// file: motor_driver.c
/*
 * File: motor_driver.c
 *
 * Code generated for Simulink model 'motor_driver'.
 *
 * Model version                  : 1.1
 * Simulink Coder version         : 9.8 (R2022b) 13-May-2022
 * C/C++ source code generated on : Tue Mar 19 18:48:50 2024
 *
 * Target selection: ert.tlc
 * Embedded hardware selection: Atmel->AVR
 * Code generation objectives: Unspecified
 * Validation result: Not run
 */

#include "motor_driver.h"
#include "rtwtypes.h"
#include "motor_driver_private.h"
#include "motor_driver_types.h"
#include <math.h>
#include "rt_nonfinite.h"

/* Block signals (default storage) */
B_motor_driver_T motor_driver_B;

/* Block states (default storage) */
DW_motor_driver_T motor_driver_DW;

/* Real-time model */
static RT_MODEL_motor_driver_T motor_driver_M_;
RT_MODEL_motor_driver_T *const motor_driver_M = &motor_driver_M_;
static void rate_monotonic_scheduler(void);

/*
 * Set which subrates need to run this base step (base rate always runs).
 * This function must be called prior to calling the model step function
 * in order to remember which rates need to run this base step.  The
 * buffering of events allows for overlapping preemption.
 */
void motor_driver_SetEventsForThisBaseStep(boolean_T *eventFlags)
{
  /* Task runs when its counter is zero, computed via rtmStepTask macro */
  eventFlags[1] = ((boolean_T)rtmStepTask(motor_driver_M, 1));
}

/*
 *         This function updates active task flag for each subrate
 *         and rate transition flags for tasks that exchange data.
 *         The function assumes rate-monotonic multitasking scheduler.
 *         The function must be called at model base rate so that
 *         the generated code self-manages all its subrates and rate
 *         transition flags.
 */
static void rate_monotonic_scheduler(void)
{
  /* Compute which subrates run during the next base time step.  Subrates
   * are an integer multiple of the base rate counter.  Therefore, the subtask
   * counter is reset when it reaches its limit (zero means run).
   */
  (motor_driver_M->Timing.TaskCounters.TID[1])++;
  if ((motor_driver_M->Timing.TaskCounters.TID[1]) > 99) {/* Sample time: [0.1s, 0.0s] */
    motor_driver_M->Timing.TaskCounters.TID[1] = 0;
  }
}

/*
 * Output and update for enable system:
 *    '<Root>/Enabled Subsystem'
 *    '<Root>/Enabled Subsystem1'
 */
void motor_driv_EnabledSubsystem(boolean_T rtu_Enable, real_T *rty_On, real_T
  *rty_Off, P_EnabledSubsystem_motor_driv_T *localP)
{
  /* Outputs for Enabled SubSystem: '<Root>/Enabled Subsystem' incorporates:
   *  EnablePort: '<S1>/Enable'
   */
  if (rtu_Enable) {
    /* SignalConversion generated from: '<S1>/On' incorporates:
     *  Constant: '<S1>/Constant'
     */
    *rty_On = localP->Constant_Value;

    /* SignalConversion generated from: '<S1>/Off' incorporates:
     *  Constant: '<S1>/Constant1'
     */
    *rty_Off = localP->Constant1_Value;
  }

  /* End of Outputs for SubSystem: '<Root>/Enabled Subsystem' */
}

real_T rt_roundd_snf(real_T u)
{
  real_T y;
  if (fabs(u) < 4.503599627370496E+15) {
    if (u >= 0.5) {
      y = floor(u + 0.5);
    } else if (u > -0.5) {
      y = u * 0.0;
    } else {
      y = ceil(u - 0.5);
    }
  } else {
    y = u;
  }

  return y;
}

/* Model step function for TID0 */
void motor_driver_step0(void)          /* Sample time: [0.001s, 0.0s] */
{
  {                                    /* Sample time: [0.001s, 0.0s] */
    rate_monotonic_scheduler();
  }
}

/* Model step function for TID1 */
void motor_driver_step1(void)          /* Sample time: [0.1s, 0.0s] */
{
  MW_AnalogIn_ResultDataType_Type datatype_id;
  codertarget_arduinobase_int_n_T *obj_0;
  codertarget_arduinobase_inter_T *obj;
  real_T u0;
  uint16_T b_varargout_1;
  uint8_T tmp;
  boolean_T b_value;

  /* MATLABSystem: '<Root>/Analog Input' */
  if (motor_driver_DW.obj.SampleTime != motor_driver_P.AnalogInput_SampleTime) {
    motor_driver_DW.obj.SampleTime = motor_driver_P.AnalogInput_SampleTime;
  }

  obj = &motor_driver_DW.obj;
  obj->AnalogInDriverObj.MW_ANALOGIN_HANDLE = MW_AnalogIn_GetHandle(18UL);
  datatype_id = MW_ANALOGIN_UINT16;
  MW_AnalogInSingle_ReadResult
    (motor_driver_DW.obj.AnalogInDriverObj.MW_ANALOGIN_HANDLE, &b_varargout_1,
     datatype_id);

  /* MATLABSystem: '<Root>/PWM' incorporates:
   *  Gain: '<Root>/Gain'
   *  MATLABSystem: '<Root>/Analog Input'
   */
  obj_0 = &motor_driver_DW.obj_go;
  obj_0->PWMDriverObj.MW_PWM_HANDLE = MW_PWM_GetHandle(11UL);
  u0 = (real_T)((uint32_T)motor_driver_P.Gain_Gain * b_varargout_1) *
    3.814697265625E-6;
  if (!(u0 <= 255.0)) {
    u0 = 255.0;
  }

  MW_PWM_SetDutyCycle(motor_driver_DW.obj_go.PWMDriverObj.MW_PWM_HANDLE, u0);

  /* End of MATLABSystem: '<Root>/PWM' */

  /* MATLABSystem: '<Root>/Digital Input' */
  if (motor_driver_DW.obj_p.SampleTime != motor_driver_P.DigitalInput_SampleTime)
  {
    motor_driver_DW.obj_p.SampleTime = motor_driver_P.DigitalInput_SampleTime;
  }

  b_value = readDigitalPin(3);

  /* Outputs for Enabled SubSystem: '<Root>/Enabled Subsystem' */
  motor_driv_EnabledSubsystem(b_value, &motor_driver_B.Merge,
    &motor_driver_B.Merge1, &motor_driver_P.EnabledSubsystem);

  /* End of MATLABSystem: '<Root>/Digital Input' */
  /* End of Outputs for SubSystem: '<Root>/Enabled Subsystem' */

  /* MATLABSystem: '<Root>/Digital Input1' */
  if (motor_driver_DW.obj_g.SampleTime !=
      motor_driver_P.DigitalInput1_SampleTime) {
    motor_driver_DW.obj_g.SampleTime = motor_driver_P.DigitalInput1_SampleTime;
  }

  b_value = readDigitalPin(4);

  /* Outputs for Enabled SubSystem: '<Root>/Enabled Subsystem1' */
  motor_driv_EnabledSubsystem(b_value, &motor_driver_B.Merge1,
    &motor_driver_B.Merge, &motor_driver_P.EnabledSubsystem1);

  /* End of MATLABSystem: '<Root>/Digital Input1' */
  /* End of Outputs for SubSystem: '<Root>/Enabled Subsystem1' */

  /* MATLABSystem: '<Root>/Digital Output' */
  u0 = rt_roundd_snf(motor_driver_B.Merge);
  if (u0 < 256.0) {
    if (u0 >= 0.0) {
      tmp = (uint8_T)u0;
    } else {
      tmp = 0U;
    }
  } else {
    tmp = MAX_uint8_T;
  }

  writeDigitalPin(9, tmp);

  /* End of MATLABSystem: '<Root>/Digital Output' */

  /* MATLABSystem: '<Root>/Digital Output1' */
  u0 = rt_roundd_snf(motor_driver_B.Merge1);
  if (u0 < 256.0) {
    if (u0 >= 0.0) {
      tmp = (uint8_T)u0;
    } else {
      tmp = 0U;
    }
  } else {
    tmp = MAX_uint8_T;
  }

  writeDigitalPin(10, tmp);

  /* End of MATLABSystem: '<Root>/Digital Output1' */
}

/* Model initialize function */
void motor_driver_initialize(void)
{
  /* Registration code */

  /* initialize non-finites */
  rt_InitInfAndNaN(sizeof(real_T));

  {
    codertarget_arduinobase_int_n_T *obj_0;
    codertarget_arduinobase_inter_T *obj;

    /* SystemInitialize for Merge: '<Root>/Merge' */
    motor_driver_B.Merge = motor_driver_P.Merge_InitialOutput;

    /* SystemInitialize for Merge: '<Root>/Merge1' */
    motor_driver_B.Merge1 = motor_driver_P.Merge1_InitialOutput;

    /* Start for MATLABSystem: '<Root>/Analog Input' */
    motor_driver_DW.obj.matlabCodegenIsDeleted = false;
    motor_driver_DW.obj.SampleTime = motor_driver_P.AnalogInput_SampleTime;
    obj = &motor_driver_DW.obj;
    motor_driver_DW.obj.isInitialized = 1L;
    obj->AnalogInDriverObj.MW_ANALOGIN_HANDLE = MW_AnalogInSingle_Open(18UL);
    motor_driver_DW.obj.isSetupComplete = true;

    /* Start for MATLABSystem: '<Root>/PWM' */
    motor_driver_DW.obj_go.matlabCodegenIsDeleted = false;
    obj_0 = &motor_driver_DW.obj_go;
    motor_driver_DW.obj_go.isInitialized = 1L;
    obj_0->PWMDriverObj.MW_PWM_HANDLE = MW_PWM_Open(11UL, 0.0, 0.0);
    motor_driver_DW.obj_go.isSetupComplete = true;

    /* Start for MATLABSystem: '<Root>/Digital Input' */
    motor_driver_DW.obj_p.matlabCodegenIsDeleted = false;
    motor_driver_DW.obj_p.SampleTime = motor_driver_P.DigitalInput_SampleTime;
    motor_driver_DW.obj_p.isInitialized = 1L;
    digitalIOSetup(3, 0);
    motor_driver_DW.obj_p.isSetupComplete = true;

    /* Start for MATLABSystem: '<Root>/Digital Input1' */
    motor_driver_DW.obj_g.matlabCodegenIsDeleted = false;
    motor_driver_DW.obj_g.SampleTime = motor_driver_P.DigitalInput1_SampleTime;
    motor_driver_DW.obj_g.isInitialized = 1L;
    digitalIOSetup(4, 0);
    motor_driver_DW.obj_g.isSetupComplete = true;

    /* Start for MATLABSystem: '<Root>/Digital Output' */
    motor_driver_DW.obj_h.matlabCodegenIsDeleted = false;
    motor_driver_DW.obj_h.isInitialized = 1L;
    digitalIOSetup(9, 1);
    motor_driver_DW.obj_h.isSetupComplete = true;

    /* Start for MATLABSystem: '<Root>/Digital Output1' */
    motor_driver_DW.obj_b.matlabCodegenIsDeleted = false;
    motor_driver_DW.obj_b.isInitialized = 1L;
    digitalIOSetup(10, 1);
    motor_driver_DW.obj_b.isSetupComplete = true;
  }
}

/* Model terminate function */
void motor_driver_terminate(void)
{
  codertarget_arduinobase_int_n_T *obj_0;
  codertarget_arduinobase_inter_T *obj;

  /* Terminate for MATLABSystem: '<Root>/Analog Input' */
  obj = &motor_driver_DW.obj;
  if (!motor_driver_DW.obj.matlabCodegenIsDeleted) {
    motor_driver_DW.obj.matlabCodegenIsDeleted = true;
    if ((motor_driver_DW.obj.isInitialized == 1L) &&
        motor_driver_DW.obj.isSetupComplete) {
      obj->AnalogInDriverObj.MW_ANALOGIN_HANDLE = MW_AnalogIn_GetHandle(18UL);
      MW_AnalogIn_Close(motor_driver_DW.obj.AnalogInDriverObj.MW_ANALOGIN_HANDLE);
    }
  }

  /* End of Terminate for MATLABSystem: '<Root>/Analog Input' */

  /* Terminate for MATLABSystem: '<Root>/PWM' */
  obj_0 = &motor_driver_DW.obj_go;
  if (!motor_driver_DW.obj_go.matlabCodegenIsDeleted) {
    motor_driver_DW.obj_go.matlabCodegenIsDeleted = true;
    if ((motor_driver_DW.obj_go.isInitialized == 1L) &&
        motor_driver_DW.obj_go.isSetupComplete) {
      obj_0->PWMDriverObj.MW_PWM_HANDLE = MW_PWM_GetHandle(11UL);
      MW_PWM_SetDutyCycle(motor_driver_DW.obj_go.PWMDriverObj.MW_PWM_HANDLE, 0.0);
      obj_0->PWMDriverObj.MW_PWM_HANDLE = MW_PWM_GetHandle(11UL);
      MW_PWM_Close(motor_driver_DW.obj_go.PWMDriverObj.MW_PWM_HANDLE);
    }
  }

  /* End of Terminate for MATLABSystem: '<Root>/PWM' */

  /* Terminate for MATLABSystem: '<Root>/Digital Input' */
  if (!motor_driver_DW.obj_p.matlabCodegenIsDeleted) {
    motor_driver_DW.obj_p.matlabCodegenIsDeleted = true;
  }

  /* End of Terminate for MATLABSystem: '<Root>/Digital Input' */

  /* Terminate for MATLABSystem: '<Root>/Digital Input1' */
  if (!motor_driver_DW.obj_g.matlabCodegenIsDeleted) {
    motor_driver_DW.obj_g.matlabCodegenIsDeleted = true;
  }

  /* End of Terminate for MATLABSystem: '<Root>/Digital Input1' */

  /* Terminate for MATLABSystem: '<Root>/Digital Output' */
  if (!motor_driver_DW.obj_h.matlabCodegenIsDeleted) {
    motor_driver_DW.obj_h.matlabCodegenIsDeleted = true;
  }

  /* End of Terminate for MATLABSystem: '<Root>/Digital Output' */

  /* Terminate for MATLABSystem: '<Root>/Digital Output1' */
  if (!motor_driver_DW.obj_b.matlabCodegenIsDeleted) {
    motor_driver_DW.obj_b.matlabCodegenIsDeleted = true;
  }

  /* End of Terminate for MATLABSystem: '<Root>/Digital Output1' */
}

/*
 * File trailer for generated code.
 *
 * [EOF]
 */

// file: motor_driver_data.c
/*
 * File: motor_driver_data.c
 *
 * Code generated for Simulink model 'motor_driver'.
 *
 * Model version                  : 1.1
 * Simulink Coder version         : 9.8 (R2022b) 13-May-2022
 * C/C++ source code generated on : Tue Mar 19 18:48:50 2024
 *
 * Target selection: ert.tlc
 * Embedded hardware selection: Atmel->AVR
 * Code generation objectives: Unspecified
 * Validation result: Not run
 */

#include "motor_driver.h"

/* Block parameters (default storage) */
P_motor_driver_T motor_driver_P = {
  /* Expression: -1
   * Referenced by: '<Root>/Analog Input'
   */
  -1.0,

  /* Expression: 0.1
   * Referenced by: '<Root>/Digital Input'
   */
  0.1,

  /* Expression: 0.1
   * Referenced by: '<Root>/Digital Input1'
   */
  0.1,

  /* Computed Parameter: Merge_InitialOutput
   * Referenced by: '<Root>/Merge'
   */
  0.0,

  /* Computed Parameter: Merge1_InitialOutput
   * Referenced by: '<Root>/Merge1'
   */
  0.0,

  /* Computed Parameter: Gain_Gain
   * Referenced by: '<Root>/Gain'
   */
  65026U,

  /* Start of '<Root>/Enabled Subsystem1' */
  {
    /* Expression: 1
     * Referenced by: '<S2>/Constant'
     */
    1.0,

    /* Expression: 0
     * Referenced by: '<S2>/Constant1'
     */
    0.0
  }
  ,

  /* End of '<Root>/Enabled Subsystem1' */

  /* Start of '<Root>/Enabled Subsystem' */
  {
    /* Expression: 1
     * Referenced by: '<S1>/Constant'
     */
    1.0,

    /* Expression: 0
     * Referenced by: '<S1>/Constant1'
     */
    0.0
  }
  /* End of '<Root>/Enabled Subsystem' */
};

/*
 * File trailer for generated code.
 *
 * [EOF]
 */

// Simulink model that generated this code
simulink model "motor_driver"  (R2022b)
settings: Solver=FixedStepDiscrete  StartTime=0.0  StopTime=10.0  FixedStep=1e-3  RelTol=1e-3  EnableMultiTasking=on
libraries: arduinolib x6

== system motor_driver ==
  Analog Input : arduinolib/Analog Input  pinNumber=4  ReadResultsOnly=off  ConversionTriggerSource=Software  ExternalTriggerType=uint32( 0 )  OutputDataType=uint16  EnableConversionCompleteNotify=off  EnableOuputStatus=off  SampleTime=-1  blockPlatform=arduino
  Digital Input : arduinolib/Digital Input  pinNumber=3  mode=Default  Direction=input  SampleTime=0.1  blockPlatform=arduino
  Digital Input1 : arduinolib/Digital Input  pinNumber=4  mode=Default  Direction=input  SampleTime=0.1  blockPlatform=arduino
  Digital Output : arduinolib/Digital Output  pinNumber=9  Direction=output  blockPlatform=arduino
  Digital Output1 : arduinolib/Digital Output  pinNumber=10  Direction=output  blockPlatform=arduino
  Display : Display
  Enabled Subsystem : Subsystem  TreatAsAtomicUnit=on
  Enabled Subsystem1 : Subsystem  TreatAsAtomicUnit=on
  Gain : Gain  Gain=255/1028
  Merge : Merge
  Merge1 : Merge
  PWM : arduinolib/PWM  pinNumber=11  frequencyType=Default  desiredFrequency=490.2  achievableFrequency=490.2
  wires:
  Digital Input1/1 -> Enabled Subsystem1/Enable
  Digital Input/1 -> Enabled Subsystem/Enable
  Enabled Subsystem/1(On) -> Merge/1
  Enabled Subsystem/2(Off) -> Merge1/2
  Enabled Subsystem1/1(On) -> Merge1/1
  Enabled Subsystem1/2(Off) -> Merge/2
  Merge/1 -> Digital Output/1
  Merge1/1 -> Digital Output1/1
  Gain/1 -> Display/1, PWM/1
  Analog Input/1 -> Gain/1

== system motor_driver/Enabled Subsystem ==
  Enable : EnablePort
  Constant : Constant
  Constant1 : Constant  Value=0
  On : Outport
  Off : Outport  Port=2
  wires:
  Constant/1 -> On/1
  Constant1/1 -> Off/1

== system motor_driver/Enabled Subsystem1 ==
  Enable : EnablePort
  Constant : Constant
  Constant1 : Constant  Value=0
  On : Outport
  Off : Outport  Port=2
  wires:
  Constant1/1 -> Off/1
  Constant/1 -> On/1
